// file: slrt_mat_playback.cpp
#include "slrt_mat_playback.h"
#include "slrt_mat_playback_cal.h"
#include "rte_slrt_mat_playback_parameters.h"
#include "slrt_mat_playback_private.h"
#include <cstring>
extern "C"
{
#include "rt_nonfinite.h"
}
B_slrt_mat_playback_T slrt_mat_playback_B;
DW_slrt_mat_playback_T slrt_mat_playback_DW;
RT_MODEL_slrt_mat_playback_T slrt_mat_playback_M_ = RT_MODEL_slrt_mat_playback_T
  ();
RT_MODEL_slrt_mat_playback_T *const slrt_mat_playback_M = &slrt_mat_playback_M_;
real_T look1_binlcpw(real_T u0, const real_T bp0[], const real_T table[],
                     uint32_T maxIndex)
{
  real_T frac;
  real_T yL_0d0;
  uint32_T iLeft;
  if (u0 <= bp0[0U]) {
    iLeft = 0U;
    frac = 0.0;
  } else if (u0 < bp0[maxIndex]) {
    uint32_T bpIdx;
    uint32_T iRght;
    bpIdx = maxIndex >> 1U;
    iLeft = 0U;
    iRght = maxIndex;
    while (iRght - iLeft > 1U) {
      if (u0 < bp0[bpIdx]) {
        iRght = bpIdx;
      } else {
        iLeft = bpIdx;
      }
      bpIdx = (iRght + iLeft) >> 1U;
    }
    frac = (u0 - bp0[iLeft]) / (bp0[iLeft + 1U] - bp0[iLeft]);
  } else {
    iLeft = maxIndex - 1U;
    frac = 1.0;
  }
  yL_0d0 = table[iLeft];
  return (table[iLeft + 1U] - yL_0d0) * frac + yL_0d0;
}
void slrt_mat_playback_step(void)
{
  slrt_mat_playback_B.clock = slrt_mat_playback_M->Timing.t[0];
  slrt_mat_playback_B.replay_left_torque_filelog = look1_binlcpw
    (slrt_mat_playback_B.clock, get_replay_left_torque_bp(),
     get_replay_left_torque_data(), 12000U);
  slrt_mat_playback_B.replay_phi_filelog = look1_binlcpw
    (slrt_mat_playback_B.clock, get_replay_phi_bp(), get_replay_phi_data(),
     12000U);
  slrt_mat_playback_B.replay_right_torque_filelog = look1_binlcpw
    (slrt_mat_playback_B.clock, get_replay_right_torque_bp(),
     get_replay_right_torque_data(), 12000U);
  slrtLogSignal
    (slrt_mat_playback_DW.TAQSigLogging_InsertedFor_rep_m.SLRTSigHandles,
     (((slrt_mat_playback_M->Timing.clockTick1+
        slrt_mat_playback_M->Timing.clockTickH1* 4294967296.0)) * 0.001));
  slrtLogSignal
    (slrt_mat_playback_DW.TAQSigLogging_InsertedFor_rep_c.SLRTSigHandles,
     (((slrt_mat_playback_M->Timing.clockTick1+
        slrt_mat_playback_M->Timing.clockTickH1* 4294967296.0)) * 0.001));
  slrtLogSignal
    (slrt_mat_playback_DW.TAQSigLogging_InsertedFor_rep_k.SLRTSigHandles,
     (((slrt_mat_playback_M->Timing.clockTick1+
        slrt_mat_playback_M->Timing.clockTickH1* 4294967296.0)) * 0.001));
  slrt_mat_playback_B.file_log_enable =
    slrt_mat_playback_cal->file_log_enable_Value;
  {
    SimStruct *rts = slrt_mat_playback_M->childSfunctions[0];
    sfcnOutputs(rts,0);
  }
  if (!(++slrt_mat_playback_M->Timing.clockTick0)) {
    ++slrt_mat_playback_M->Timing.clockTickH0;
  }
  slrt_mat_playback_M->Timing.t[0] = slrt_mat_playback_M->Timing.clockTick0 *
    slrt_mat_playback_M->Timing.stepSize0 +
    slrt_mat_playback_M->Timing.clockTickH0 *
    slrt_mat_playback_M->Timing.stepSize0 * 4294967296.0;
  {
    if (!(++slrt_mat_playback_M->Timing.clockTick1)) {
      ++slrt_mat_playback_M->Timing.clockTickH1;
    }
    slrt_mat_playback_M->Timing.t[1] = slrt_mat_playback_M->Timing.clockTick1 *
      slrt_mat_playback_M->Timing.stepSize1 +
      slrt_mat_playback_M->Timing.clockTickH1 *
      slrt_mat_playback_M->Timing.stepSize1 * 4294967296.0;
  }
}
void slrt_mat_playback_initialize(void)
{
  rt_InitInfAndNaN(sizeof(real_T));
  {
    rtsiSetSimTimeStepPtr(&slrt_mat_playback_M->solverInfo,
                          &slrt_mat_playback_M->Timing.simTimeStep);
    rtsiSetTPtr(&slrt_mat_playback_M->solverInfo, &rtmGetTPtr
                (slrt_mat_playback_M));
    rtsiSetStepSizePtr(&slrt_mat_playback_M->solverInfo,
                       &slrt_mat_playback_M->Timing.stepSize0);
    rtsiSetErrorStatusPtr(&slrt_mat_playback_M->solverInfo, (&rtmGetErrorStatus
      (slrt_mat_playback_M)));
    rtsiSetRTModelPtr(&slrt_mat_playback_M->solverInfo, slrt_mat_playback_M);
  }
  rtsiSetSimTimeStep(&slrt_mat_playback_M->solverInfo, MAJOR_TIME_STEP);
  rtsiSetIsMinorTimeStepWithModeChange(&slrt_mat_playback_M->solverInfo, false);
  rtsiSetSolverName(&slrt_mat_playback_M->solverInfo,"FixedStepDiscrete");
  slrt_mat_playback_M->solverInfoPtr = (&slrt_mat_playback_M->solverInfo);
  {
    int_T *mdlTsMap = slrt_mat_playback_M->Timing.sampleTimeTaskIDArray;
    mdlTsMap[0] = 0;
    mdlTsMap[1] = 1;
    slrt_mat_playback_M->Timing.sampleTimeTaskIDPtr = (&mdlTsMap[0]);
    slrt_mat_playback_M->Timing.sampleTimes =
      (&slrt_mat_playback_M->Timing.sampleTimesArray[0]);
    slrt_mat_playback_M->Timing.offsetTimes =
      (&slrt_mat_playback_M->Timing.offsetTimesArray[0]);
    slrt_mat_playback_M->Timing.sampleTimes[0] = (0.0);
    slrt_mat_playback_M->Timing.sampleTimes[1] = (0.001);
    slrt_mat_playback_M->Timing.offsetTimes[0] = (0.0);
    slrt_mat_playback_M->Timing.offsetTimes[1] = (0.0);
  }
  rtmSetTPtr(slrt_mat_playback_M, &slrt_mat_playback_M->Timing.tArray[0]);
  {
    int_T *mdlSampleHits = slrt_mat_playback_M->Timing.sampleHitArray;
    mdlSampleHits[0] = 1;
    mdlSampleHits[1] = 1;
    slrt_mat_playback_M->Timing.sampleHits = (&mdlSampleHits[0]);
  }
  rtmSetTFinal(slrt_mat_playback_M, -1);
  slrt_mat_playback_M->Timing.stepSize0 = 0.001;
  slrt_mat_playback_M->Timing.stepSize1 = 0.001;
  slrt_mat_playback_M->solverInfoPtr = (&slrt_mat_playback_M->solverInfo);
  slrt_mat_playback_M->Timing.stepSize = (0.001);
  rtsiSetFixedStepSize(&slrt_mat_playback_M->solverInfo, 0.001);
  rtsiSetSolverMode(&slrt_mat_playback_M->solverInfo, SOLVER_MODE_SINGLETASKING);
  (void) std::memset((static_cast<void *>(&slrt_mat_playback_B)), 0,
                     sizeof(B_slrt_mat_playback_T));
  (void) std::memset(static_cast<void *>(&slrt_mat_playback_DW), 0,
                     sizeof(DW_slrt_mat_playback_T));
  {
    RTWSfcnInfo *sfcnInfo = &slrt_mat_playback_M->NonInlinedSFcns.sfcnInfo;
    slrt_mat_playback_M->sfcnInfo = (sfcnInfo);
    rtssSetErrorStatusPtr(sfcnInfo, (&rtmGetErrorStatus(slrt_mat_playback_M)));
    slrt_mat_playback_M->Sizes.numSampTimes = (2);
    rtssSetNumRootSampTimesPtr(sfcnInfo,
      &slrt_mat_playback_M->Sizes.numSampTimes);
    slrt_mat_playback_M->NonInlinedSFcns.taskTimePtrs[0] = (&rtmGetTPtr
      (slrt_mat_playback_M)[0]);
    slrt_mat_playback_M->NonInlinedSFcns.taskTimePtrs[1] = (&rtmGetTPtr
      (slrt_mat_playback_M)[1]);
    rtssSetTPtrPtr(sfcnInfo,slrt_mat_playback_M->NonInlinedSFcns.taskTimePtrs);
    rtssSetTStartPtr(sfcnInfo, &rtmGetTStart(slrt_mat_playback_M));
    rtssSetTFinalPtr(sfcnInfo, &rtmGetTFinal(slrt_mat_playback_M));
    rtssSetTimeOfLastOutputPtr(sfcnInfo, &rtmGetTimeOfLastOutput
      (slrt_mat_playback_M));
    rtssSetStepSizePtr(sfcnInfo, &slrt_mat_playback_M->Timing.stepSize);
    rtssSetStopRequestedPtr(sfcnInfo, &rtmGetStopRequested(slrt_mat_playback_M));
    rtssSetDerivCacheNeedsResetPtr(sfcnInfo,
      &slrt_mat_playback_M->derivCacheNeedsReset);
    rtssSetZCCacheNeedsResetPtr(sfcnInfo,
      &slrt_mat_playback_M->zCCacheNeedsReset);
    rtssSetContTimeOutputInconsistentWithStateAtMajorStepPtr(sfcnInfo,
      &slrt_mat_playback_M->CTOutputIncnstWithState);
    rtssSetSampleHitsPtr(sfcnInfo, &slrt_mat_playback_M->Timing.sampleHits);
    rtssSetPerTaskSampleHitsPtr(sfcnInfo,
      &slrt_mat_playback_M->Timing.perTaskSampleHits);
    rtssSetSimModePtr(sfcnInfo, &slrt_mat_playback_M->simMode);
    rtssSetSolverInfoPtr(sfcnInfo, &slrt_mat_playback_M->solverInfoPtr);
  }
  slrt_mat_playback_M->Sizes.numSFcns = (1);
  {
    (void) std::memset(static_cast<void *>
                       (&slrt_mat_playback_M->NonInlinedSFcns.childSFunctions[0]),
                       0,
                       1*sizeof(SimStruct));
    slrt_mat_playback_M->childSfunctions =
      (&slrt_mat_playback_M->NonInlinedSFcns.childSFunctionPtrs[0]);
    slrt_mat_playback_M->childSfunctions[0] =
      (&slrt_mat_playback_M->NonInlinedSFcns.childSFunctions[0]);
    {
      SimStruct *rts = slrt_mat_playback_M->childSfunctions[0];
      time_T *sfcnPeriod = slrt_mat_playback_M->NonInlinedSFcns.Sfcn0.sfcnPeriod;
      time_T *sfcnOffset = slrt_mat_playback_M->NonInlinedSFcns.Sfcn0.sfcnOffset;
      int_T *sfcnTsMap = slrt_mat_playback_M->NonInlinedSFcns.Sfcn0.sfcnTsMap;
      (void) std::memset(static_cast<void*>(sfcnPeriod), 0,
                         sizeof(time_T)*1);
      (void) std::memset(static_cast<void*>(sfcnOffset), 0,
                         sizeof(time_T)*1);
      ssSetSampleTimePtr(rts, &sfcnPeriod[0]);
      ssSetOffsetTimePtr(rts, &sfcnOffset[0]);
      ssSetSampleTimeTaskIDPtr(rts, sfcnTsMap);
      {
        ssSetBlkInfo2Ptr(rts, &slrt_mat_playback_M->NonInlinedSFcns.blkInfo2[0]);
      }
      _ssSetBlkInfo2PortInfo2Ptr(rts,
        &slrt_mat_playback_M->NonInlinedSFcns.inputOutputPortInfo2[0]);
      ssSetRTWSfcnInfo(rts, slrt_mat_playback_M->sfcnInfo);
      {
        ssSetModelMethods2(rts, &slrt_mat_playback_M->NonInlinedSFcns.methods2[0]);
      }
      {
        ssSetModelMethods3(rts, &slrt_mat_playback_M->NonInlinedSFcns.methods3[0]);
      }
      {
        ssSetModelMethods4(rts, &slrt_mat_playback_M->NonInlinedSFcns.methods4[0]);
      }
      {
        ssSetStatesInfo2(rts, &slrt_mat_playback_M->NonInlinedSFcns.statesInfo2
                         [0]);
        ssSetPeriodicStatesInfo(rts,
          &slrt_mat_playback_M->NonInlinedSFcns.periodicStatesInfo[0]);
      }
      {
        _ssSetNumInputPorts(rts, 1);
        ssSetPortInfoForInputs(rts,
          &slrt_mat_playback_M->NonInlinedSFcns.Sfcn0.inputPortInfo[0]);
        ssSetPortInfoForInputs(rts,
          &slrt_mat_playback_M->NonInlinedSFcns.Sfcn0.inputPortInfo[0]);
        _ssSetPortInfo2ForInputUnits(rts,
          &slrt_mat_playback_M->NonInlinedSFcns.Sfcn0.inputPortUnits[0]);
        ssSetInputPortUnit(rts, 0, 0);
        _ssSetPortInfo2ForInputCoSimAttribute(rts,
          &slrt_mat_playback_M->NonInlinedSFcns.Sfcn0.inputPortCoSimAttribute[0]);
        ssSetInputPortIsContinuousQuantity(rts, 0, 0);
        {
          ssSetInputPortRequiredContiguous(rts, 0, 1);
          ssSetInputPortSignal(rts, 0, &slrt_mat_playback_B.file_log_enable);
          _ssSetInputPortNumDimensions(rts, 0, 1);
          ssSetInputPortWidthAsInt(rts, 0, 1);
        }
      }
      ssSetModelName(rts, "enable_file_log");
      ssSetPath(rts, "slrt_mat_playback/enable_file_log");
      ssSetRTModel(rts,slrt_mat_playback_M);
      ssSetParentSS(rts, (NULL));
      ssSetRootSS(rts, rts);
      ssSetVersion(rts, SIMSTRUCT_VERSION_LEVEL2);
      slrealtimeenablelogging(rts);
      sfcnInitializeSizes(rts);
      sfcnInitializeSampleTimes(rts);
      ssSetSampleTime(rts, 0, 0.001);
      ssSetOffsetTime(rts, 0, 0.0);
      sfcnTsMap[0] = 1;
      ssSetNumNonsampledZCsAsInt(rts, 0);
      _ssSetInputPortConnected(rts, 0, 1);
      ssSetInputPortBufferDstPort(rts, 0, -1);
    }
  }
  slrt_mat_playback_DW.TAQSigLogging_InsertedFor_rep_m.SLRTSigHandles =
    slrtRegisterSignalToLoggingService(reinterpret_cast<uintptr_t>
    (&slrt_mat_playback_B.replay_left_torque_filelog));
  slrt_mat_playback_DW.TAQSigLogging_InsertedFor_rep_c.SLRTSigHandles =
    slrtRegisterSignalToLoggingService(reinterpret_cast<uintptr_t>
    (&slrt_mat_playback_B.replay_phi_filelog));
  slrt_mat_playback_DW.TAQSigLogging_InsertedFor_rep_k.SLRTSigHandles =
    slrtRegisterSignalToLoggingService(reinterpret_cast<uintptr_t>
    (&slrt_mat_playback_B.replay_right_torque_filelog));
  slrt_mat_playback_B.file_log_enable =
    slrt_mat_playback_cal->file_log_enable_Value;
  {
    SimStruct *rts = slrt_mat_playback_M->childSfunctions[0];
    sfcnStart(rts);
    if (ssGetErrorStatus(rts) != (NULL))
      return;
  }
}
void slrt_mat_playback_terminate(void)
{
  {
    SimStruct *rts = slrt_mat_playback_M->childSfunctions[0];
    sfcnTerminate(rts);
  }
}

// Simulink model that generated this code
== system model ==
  FileLog#1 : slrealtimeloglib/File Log  <- 1: Lookup_nD#1
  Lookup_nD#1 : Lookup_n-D  BreakpointsForDimension1=replay_left_torque_bp  Table=replay_left_torque_data  <- 1: clock
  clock : Clock
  FileLog#2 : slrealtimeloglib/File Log  <- 1: Lookup_nD#2
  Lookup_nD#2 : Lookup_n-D  BreakpointsForDimension1=replay_phi_bp  Table=replay_phi_data  <- 1: clock
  FileLog#3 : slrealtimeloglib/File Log  <- 1: Lookup_nD#3
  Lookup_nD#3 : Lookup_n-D  BreakpointsForDimension1=replay_right_torque_bp  Table=replay_right_torque_data  <- 1: clock
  enable_file_log : slrealtimeloglib/Enable File Log  <- 1: file_log_enable
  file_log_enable : Constant  Value=true
